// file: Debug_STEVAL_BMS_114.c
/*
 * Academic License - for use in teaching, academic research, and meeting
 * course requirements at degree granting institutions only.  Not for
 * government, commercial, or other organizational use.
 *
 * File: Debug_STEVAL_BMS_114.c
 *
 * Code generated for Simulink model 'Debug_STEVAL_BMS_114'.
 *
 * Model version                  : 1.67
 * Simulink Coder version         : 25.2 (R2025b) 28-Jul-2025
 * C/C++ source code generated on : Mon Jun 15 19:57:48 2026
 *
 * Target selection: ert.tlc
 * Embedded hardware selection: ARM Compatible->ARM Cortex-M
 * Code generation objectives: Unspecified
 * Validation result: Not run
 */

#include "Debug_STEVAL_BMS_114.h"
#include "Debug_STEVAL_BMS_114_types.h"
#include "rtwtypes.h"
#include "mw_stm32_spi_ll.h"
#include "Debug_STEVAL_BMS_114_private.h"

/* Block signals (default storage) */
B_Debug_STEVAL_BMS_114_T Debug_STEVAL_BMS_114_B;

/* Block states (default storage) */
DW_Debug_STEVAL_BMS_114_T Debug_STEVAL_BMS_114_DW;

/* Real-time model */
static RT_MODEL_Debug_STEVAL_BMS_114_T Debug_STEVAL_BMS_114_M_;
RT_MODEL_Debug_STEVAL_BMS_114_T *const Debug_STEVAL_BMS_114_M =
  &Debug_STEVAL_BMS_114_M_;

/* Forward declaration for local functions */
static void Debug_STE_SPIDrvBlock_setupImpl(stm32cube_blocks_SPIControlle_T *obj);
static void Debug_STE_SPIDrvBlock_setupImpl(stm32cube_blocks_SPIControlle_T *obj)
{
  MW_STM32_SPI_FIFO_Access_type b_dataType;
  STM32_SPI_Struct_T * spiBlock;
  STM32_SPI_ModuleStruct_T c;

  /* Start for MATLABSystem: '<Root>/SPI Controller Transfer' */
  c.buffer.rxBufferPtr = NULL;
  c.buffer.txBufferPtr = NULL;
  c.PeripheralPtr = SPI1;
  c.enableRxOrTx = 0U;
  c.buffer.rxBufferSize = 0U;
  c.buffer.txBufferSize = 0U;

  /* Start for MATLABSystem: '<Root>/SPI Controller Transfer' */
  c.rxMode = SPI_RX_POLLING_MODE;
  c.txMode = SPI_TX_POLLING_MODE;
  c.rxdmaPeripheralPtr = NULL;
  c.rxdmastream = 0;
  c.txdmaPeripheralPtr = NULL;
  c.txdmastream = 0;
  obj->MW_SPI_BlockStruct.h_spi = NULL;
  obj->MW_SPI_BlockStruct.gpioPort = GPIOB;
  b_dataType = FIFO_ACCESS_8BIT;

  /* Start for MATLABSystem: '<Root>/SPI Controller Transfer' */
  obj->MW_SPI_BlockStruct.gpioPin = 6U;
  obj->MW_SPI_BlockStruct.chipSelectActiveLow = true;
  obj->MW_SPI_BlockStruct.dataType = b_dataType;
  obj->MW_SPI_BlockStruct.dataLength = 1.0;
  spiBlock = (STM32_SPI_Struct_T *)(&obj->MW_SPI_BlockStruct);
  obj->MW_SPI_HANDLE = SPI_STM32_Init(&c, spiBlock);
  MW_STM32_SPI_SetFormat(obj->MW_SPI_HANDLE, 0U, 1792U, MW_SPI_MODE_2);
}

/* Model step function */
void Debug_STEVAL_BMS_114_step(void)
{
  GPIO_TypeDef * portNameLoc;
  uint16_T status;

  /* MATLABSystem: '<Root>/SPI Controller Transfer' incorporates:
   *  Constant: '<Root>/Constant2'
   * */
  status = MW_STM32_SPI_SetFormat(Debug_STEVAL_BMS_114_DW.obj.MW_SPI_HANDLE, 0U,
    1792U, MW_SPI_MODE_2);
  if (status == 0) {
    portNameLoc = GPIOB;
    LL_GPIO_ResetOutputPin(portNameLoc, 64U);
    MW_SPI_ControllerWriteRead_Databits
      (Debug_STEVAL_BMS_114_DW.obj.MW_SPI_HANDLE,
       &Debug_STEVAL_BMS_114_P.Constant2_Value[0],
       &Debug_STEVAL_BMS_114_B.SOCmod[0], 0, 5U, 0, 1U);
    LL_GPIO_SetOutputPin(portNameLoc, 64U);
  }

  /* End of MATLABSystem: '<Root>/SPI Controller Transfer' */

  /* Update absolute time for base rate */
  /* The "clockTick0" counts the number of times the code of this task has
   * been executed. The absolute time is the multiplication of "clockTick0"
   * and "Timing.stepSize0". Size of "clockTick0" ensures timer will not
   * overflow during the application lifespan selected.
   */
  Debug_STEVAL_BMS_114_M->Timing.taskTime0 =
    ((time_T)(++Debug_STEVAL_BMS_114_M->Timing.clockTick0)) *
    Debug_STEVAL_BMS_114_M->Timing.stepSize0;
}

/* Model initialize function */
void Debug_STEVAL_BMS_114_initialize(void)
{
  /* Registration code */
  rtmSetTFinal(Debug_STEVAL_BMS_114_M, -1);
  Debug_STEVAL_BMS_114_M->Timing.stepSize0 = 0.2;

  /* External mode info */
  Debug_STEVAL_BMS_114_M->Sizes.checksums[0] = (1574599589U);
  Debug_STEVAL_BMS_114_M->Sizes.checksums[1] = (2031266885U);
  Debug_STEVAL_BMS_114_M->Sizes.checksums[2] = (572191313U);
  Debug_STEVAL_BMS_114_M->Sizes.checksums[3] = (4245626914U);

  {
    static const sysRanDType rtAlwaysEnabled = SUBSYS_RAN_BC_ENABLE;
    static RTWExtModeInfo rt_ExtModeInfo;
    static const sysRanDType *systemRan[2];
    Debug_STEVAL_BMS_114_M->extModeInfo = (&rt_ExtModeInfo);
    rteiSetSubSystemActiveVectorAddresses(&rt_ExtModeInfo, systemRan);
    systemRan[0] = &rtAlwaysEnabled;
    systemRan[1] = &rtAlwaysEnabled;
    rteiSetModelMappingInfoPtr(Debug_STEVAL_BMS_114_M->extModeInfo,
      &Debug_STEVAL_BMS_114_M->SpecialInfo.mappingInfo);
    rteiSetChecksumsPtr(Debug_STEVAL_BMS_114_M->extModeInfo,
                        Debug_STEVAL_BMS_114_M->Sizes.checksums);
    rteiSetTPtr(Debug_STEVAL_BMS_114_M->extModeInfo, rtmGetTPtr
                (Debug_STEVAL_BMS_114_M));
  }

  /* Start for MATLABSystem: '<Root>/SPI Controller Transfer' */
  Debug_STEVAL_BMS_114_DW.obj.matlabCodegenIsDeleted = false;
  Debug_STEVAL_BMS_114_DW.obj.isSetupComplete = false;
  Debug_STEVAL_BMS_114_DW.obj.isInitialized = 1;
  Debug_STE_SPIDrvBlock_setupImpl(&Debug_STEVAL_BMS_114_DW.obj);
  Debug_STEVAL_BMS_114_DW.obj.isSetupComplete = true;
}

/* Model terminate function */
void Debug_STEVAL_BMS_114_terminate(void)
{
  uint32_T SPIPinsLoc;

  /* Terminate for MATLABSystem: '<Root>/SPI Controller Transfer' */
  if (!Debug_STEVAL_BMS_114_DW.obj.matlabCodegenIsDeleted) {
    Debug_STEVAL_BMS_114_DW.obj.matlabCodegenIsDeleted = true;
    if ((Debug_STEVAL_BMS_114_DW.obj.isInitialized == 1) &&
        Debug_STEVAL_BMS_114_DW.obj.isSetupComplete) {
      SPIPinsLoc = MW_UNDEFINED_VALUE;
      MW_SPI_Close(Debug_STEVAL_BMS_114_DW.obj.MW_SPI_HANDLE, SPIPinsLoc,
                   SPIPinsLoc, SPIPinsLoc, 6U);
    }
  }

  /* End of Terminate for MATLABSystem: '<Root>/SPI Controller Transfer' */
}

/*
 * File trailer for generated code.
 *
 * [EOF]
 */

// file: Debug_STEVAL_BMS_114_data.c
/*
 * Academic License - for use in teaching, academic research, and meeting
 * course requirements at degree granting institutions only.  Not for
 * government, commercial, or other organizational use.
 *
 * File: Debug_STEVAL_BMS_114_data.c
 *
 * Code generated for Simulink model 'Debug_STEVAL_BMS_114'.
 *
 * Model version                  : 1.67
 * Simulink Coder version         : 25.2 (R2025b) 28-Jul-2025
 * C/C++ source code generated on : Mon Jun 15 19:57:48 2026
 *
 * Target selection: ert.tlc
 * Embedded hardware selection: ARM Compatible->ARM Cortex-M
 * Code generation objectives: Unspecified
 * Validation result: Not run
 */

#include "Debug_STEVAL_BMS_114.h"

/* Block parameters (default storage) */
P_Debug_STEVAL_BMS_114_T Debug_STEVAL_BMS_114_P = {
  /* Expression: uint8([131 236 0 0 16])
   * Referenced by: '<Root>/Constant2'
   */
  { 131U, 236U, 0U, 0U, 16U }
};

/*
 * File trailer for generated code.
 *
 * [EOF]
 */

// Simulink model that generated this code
simulink model "Debug_STEVAL_BMS_114"  (R2025b)
settings: Solver=FixedStepAuto  StartTime=0.0  StopTime=inf  MaxStep=.01  RelTol=1e-3  EnableMultiTasking=on
PreLoadFcn:
  | %setup_sil;
  | setup_pil;
InitFcn:
  | battery_init;
  | Full_Charge_Volt=4.2; % unit volts
  | Cutoff_Volt=3; % unit volts
  | Delta=.02;
  | ContactorTime=20;
  | ContactorTimeOut=100;
  | High_TempLim=333;
  | Low_TempLim=263;
  | Sensor_Fault_Treshold=.02;
  | CurrentTimeout=1;
  | Allowed_Delta=.04;
  | Bal_On_Time=30;
  | Bal_Off_Time=5;
  | BalNotAct_Time=10;
libraries: stm32blockslib x1

== system Debug_STEVAL_BMS_114 ==
  Constant2 : Constant  Value=uint8([192 4 8 0 21])
  SPI Controller Transfer : stm32blockslib/SPI Controller Transfer  SPIModuleSelect=SPI1  ClockPolarity=Low  ClockPhase=1 Edge  SPIModule=uint32(0)  Mode=Master  BusSpeed=uint32(1000000)  FirstBitToTransfer=Most significant bit (MSB)  ClockMode=0  BlockFunction=Transfer  EnableRegisterAddress=off  RegisterAddress=0  OutputDataType=uint8  OutputDataLength=1  OutputStatus=off  BlockingMode=off  Timeout=0.001  DataBits=8  UseCustomSSPin=Explicit GPIO calls  ActiveLowSSPin=Active low  Port_Select=GPIOB  Pin=6
  Scope5 : Scope
  wires:
  SPI Controller Transfer/1 -> Scope5/1  "SOCmod"
  Constant2/1 -> SPI Controller Transfer/1
